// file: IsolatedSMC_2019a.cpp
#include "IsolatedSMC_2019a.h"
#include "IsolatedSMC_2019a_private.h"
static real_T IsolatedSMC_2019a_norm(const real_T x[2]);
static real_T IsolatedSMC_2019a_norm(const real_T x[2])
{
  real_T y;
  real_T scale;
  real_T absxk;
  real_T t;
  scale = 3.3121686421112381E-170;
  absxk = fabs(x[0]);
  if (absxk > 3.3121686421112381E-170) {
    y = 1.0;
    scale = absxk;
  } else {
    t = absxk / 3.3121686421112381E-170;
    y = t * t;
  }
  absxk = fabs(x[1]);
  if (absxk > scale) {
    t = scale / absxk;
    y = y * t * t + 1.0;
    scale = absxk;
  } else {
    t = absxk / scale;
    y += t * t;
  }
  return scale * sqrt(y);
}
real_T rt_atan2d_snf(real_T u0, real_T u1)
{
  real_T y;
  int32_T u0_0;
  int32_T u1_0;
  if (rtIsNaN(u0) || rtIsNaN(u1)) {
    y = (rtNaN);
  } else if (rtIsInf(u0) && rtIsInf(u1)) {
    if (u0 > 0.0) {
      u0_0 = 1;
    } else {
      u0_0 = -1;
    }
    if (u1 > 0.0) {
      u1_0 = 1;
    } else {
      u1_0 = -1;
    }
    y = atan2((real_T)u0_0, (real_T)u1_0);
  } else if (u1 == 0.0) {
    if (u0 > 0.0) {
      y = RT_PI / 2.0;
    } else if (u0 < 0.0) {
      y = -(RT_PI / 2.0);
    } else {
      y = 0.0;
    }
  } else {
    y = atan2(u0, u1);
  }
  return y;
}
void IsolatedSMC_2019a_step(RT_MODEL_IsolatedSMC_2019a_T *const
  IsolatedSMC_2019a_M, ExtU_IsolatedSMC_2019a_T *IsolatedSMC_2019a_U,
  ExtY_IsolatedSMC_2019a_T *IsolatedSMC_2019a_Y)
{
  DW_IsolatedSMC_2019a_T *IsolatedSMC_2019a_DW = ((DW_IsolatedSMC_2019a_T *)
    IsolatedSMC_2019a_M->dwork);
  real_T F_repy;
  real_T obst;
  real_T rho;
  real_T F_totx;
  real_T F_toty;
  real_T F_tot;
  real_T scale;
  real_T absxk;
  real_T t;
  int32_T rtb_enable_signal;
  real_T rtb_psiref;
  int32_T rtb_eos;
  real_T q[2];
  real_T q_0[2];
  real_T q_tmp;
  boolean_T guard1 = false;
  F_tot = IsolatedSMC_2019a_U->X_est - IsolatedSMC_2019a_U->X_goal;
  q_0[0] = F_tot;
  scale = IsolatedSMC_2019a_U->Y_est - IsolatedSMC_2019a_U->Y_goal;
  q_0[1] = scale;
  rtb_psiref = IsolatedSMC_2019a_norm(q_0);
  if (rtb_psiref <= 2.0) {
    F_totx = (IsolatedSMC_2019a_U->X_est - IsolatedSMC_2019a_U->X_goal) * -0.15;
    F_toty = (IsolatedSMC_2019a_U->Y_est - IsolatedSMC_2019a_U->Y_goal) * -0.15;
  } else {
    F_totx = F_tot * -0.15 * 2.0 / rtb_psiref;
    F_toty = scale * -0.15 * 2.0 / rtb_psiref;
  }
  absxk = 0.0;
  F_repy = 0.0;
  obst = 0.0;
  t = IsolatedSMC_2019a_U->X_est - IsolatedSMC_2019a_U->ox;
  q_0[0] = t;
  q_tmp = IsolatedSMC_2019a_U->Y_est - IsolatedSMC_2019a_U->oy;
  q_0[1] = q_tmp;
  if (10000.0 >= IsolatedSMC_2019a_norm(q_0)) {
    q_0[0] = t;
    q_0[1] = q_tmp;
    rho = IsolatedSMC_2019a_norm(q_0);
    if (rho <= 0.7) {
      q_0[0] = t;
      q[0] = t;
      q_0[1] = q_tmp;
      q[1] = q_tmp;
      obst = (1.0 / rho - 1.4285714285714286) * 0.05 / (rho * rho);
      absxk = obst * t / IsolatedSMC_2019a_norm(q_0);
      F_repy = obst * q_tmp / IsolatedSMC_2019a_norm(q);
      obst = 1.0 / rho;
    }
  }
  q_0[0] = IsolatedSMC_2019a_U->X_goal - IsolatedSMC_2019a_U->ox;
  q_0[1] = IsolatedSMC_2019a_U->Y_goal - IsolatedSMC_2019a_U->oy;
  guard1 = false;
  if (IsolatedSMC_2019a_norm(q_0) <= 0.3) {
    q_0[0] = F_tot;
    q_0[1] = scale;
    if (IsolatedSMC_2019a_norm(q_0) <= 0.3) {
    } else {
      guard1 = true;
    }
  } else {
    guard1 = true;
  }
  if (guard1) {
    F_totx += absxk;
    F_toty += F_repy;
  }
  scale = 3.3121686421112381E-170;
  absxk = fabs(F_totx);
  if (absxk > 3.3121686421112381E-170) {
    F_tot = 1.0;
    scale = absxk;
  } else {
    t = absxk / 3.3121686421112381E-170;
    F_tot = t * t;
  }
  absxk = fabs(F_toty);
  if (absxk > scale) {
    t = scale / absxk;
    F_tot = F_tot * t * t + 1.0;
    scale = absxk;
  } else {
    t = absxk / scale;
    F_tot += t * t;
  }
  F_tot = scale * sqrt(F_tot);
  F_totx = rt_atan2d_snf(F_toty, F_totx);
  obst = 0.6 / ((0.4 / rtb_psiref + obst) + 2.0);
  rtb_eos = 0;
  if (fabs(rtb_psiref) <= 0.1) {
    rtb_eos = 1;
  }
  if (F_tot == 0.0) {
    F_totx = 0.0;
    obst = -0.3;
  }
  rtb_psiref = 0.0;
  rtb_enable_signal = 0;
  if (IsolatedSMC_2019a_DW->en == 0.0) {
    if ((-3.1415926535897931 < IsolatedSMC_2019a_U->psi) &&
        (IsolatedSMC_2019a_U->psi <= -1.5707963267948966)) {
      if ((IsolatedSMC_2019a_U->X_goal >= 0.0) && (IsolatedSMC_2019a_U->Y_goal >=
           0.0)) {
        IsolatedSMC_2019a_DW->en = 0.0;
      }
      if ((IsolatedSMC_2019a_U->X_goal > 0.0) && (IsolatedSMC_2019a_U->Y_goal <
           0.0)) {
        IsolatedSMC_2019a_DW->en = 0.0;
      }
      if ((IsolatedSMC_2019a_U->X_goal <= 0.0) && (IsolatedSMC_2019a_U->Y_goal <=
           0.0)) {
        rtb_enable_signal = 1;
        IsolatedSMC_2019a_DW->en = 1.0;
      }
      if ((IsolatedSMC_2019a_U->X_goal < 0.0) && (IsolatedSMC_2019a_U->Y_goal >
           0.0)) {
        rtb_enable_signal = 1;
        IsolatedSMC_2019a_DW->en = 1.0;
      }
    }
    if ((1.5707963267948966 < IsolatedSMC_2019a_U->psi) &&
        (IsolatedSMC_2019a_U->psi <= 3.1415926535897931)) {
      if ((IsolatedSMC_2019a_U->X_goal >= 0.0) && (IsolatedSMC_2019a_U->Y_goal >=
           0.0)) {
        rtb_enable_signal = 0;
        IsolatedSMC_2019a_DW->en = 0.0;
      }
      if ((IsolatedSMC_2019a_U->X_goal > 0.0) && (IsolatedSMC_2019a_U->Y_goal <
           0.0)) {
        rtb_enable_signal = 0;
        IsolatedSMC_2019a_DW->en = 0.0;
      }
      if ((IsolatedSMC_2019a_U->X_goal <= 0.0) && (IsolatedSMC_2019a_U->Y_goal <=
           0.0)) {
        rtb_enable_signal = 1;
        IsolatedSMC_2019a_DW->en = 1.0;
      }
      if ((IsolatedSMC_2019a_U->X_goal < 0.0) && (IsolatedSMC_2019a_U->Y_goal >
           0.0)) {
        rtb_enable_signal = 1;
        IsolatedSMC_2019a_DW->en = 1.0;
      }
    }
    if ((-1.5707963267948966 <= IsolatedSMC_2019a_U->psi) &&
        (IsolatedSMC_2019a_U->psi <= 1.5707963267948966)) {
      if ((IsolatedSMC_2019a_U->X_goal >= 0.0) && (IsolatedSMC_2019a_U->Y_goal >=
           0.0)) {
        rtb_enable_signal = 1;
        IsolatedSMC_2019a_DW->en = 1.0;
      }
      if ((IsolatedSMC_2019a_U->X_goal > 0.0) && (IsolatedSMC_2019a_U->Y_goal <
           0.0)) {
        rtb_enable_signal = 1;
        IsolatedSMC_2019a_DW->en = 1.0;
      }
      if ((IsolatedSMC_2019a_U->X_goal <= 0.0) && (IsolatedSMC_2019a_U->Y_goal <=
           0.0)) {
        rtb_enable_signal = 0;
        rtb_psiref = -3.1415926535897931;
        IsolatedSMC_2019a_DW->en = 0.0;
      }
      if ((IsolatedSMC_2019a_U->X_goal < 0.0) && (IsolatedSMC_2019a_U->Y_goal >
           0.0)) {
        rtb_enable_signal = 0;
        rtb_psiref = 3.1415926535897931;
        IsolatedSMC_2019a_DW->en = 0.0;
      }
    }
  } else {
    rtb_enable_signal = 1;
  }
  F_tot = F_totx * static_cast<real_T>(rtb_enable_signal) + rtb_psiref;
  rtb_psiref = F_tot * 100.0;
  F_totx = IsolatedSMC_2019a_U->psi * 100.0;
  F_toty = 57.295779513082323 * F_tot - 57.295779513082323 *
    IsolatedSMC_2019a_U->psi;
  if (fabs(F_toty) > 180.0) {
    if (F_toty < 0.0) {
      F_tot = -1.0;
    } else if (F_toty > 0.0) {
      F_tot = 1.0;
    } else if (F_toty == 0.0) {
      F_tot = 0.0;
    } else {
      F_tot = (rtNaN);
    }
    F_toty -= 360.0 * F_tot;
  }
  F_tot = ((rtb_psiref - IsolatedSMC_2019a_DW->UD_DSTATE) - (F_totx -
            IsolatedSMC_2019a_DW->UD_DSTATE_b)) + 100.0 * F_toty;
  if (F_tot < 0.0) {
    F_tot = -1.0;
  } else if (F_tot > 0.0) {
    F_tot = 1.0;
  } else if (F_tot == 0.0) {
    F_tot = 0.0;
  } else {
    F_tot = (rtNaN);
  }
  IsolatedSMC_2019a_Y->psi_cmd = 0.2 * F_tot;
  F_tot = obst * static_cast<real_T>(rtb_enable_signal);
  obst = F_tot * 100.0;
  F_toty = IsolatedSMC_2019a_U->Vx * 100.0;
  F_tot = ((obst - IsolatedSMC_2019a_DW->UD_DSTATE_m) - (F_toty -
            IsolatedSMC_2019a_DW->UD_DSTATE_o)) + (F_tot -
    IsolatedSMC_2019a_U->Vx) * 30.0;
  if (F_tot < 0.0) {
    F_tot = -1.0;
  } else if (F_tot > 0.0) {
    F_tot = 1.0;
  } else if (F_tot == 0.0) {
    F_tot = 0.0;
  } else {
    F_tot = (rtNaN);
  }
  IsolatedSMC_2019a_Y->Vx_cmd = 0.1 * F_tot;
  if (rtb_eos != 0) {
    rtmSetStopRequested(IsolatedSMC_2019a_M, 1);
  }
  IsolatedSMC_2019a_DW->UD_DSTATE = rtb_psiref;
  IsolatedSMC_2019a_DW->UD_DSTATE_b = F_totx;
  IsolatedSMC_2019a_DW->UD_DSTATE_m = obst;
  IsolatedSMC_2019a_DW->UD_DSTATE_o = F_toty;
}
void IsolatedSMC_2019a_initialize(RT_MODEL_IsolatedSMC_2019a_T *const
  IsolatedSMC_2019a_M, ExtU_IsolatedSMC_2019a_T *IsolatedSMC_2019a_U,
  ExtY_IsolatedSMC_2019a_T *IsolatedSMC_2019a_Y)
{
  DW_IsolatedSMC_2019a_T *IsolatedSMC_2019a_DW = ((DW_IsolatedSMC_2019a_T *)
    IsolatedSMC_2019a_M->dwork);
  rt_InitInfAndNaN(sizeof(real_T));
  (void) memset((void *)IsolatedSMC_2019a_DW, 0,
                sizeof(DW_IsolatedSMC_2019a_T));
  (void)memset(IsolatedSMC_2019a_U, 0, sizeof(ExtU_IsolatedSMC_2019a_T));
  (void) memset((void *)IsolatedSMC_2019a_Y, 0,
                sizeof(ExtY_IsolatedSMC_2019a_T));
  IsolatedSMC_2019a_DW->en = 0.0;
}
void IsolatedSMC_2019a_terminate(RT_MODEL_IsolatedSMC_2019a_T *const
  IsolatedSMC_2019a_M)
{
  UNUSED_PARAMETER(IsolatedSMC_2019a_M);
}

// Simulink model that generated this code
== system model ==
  psi : Inport
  Vx : Inport
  X_est : Inport
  Y_est : Inport
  X_goal : Inport
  Y_goal : Inport
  ox : Inport
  oy : Inport
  Vx_cmd : Outport  <- 1: MATLABFunction#1
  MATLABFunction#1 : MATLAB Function  <- 1: Sum#1, 2: Sum#2
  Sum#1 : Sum  Inputs=+-  <- 1: DiscreteDerivative#1, 2: DiscreteDerivative#2
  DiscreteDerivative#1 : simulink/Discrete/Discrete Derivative  gainval=1.0  <- 1: Product#1
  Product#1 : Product  <- 1: MATLABFunction#2, 2: MATLABFunction#3
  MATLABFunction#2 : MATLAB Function  <- 1: X_est, 2: Y_est, 3: X_goal, 4: Y_goal, 5: ox, 6: oy, 7: Constant#1
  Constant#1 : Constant  Value=0.1
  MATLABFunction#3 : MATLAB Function  <- 1: X_goal, 2: Y_goal, 3: psi
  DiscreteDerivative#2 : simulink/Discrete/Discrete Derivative  gainval=1.0  <- 1: Vx
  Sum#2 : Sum  Inputs=+-  <- 1: Product#1, 2: Vx
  psi_cmd : Outport  <- 1: MATLABFunction#4
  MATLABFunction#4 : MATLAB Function  <- 1: Sum#3, 2: MATLABFunction#5
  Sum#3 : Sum  Inputs=+-  <- 1: DiscreteDerivative#3, 2: DiscreteDerivative#4
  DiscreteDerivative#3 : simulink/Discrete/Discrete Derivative  gainval=1.0  <- 1: Sum#4
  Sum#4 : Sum  Inputs=++  <- 1: Product#2, 2: MATLABFunction#3/2
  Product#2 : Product  <- 1: MATLABFunction#2/2, 2: MATLABFunction#3
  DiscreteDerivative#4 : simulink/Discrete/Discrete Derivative  gainval=1.0  <- 1: psi
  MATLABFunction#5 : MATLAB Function  <- 1: Gain#1, 2: Gain#2
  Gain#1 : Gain  Gain=180/pi  <- 1: Sum#4
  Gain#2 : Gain  Gain=180/pi  <- 1: psi
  Stop#1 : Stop  <- 1: CompareToZero#1
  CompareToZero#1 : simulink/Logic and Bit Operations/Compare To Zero  relop===  <- 1: CompareToZero#2
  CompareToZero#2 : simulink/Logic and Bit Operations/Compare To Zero  relop===  <- 1: MATLABFunction#2/8
== matlab function MATLAB Function ==
function [enable_signal, psiref] = fcn(X_goal, Y_goal, psi_est)
psiref=0;
enable_signal=0;

persistent en
if isempty(en)
    en=0;
end

if en==0
if -pi<psi_est && psi_est<=-pi/2 
  if X_goal>=0 && Y_goal>=0
      enable_signal=0;
      psiref=0;
      en=0;
  end
   if X_goal>0 && Y_goal<0
      enable_signal=0;
      psiref=0;
      en=0;
   end
    if X_goal<=0 && Y_goal<=0
      enable_signal=1;
      en=1;
      psiref=0;
    end
    if X_goal<0 && Y_goal>0
      enable_signal=1;
      en=1;
      psiref=0;
    end
end
if pi/2<psi_est && psi_est<=pi 
  if X_goal>=0 && Y_goal>=0
      enable_signal=0;
      psiref=0;
      en=0;
  end
   if X_goal>0 && Y_goal<0
      enable_signal=0;
      psiref=0;
      en=0;
   end
    if X_goal<=0 && Y_goal<=0
      enable_signal=1;
      en=1;
      psiref=0;
    end
    if X_goal<0 && Y_goal>0
      enable_signal=1;
      en=1;
      psiref=0;
    end
end

if -pi/2<=psi_est && psi_est<=pi/2
  if X_goal>=0 && Y_goal>=0
      enable_signal=1;
      en=1;
      psiref=0;
  end
   if X_goal>0 && Y_goal<0
      enable_signal=1;
      en=1;
      psiref=0;
   end
    if X_goal<=0 && Y_goal<=0
      enable_signal=0;
      psiref=-pi;
      en=0;
    end
    if X_goal<0 && Y_goal>0
      enable_signal=0;
      psiref=pi;
      en=0;
    end
end
else
    enable_signal=1;
    psiref=0;
end

== matlab function MATLABFunction#1 ==
function Vx_cmd = SMC_Vx(Ax_err, Vx_err)
% SMC params
lamda = 30;
K = 0.1;
% Sliding surface
s = zeros(1);
s = (Ax_err) + lamda*(Vx_err);

Vx_cmd = K*sign(s);

== matlab function MATLAB Function ==
function errore = fcn(psi_ref, psi_est)
errore=psi_ref-psi_est;

if abs(errore)>180
    errore=errore-360*sign(errore);
end

== matlab function MATLABFunction#2 ==
function [V_ref, psi_ref, rho_goal, F_repx, F_repy, F_attx, F_atty, eos]  = fcn(X_est, Y_est, X_goal, Y_goal,  ox, oy, Toll_to_end)

% Potential field characteristics
rho_0=0.7;                   % Area of influence of obstacle  [m]
kp = 0.15;                   % Attractive pottential gain
eta = 0.05;                  % Repulsive potential gain

q=[X_est, Y_est]';           % Actual position [m]       
qg=[X_goal, Y_goal]';        % Goal position   [m]
rho_goal=norm(q-qg,2);       % Distance actual position-goal position
d=2;                         % Distance from goal, point of attractive field characteristic switching

% ATTRACTIVE
if rho_goal<=d
F_attx = -kp*(X_est-X_goal);
F_atty = -kp*(Y_est-Y_goal);
else    
F_attx = -kp*(X_est-X_goal)*d/rho_goal;
F_atty = -kp*(Y_est-Y_goal)*d/rho_goal;
end

% REPULSIVE
F_repx=0;
F_repy=0;
dmin=10000;
qc=[0 0]';
obst=0;

for k=1:length(ox)
    qc=[ox(k) oy(k)]';                          % Obstacle position [m]
    dq = norm(q-qc,2);                          % Distance actual position- obstacle position
     
    if dmin >= dq
        dmin = dq;
        min_ost = k;
        qc=[ox(min_ost) oy(min_ost)]';
        rho = norm(q-qc,2) ;                    % Distance with the nearest obstacle
        
        if rho<=rho_0                           % Inside obstacle area! Danger
           F_repx=eta*(1/rho - 1/rho_0)*1/(rho).^2*(X_est-ox(min_ost))/norm(q-qc,2);
           F_repy=eta*(1/rho - 1/rho_0)*1/(rho).^2*(Y_est-oy(min_ost))/norm(q-qc,2);  
           obst=1/rho;
        end
     
     end
end

% To find the goal if the obstacle is near
dob=0.3;
dgr=0.3;

if norm(qg-qc,2)<=dob && norm(q-qg,2)<=dgr
    F_totx=F_attx;
    F_toty=F_atty;
else
    F_totx = F_attx+F_repx;
    F_toty = F_atty+F_repy;
end

% Potential Force
F_tot=norm([F_totx,F_toty]);

% ORIENTATION REFERENCE SIGNAL
psi_ref=atan2(F_toty,F_totx);

% VELOCITY REFERENCE SIGNAL
% 1° prova per il campo di velocità
% V_ref=F_totx/F_tot*0.3;

% 2° prova per il campo di velocità
delta=0.4/rho_goal+obst;
V_ref= 0.3*2/(2+delta);

eos = 0;
% END OF SIMULATION
if abs(rho_goal)<=Toll_to_end
    eos=1;
end

% Mathematical minimum
if F_tot==0
    psi_ref=0;
    V_ref=-0.3;
end

== matlab function MATLABFunction#4 ==
function psi_cmd = SMC_psi(psidot_error, psi_error)
% SMC params
lamda = 100;
K = 0.2;
% Sliding surface
s = zeros(1);
s = (psidot_error) + lamda*(psi_error);

psi_cmd = K*sign(s);
